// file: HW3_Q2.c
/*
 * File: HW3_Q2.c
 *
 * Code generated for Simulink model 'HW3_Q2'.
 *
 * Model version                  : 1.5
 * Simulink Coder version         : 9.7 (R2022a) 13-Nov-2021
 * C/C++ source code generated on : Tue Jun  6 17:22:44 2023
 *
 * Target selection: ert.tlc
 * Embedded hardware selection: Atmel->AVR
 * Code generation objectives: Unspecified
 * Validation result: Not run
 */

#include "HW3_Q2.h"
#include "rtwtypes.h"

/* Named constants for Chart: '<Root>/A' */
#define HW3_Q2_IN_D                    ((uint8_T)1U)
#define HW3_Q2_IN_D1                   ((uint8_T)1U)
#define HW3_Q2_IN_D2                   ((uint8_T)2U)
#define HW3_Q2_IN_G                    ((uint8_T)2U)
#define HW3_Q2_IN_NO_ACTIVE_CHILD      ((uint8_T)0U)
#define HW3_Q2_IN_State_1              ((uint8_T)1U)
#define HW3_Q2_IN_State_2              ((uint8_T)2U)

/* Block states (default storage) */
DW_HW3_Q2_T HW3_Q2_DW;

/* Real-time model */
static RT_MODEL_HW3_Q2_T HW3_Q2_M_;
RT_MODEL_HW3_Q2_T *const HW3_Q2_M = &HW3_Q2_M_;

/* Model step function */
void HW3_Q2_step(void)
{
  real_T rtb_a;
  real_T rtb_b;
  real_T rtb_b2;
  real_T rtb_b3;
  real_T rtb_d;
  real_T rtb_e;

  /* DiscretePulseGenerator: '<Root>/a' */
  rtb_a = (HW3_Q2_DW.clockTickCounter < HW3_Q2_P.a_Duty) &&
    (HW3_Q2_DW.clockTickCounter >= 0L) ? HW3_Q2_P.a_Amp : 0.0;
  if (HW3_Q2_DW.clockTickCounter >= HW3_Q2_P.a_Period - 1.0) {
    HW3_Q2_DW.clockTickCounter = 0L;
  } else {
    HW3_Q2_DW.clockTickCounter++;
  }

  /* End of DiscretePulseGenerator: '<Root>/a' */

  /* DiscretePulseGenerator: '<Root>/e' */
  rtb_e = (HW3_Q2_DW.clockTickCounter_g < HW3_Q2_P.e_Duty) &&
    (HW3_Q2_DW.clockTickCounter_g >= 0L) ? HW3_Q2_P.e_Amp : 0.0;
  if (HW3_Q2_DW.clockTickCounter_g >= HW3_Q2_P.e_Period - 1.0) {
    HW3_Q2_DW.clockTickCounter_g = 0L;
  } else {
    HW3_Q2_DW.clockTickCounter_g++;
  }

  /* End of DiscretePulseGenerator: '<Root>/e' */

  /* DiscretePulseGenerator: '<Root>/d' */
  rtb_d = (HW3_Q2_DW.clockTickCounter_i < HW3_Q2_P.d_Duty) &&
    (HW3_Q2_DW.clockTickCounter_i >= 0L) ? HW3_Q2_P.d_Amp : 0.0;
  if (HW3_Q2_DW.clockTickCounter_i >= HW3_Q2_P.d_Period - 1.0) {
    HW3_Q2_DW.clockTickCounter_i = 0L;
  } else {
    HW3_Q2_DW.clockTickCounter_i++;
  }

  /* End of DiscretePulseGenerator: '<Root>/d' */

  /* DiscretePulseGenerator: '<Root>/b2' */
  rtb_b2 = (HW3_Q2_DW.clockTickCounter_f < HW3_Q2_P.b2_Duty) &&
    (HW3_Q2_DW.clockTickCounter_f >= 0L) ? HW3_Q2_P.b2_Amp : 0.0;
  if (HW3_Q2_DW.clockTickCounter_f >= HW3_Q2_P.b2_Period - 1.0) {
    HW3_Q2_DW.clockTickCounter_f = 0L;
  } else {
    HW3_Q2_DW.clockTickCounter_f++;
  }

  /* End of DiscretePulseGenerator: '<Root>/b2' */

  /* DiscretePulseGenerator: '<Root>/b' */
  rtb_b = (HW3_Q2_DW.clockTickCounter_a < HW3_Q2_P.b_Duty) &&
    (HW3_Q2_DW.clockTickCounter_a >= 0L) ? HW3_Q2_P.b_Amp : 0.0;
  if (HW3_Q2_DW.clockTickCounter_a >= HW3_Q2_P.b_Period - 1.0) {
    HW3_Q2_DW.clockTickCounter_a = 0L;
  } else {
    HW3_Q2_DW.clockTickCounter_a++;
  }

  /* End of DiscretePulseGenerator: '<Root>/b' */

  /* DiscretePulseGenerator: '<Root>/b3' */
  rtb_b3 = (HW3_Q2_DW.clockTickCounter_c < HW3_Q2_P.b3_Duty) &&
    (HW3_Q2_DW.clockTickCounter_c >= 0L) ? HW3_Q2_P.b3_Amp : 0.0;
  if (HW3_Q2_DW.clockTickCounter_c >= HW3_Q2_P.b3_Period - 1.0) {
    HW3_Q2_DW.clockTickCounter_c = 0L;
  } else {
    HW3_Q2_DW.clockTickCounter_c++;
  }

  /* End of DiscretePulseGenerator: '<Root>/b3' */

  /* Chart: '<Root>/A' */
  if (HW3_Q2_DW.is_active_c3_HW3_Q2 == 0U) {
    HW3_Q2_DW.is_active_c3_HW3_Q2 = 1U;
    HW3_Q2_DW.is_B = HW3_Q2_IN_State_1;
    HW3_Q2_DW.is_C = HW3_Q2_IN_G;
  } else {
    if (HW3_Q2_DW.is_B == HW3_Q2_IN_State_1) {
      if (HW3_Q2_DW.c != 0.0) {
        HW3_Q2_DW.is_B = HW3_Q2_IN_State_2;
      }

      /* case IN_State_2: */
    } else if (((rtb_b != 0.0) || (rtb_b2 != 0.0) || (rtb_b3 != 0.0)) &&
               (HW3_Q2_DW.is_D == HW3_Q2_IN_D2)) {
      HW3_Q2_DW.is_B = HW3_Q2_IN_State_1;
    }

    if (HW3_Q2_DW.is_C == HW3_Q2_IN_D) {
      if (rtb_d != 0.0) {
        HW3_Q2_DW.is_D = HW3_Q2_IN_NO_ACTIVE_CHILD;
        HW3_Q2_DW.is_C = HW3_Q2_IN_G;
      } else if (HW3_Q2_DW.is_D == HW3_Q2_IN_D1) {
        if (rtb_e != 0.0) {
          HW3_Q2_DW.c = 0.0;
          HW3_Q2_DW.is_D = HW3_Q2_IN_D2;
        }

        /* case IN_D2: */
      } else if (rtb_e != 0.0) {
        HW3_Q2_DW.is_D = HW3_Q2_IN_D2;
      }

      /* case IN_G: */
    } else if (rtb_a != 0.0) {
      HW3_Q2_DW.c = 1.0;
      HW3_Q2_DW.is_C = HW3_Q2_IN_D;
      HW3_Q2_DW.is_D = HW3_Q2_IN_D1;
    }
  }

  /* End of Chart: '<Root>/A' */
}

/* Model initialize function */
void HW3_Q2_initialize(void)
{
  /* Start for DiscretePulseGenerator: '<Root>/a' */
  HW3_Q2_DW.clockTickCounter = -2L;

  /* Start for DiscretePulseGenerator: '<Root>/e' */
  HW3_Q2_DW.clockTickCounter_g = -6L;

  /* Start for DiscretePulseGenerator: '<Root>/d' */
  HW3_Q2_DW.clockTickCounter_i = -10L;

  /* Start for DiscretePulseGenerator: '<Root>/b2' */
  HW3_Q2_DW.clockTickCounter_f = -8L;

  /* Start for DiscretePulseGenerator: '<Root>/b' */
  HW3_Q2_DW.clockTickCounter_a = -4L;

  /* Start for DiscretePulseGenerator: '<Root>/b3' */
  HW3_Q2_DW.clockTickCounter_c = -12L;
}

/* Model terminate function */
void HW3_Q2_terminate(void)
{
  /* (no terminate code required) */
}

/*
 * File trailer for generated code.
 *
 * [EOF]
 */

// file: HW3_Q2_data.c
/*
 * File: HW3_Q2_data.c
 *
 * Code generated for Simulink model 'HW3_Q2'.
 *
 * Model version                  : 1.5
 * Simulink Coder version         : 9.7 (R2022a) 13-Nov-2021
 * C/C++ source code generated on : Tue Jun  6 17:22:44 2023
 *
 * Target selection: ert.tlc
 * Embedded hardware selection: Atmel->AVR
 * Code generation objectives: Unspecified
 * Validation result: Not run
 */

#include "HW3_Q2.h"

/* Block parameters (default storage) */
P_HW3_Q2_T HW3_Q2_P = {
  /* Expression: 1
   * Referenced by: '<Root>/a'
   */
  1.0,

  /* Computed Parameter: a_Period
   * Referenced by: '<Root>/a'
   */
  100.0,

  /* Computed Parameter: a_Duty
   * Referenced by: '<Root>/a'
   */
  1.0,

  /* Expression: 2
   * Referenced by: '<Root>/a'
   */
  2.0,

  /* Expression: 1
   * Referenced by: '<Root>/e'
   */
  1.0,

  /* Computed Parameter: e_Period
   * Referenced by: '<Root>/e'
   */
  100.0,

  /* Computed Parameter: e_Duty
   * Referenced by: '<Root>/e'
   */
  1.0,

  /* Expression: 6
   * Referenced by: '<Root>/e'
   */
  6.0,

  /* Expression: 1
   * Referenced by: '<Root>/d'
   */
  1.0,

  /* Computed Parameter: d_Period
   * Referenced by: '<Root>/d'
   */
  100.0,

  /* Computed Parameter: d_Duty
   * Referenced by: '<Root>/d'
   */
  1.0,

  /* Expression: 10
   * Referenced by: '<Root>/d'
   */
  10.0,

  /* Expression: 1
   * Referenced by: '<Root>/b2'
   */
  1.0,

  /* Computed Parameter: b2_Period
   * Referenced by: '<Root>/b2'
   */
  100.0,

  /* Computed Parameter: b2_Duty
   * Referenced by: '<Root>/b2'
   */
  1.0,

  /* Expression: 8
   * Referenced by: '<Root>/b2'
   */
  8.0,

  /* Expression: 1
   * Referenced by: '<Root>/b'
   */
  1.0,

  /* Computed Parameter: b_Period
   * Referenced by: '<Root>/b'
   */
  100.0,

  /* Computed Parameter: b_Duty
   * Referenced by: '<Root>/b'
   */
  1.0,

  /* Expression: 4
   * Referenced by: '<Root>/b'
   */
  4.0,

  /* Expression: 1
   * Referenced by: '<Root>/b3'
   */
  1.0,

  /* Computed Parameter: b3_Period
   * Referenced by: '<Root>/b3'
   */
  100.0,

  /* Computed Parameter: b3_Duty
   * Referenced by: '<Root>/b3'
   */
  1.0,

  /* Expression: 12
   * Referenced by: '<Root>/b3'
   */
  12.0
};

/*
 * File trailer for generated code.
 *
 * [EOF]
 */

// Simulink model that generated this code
simulink model "HW3_Q2"  (R2022a)
settings: Solver=FixedStepDiscrete  StartTime=0.0  StopTime=20  FixedStep=1  RelTol=1e-3  EnableMultiTasking=on

== system HW3_Q2 ==
  A : Stateflow chart  TreatAsAtomicUnit=on
  a : DiscretePulseGenerator  PulseType=Time based  Period=100  PhaseDelay=2
  b : DiscretePulseGenerator  PulseType=Time based  Period=100  PhaseDelay=4
  b2 : DiscretePulseGenerator  PulseType=Time based  Period=100  PhaseDelay=8
  b3 : DiscretePulseGenerator  PulseType=Time based  Period=100  PhaseDelay=12
  d : DiscretePulseGenerator  PulseType=Time based  Period=100  PhaseDelay=10
  e : DiscretePulseGenerator  PulseType=Time based  Period=100  PhaseDelay=6
  wires:
  a/1 -> A/1(a)
  b/1 -> A/5(b)
  e/1 -> A/2(e)
  b2/1 -> A/4(b2)
  d/1 -> A/3(d)
  b3/1 -> A/6(b3)

== stateflow chart HW3_Q2/A ==
  state B [parallel]
    settings: executionOrder=1
    state State_1
    state State_2
    (default) -> State_1
    State_1 -> State_2 : [c]
    State_2 -> State_1 : [(b || b2 || b3) && in(C.D.D2)]
  state C [parallel]
    settings: executionOrder=2
    state D
      state D1
      state D2
      (default) -> D1
      D1 -> D2 : [e]{c = 0;}
      D2 -> D2 : [e]
    state G
    G -> D : [a]{c = 1;}
    (default) -> G
    D -> G : [d]
  data: a input; e input; d input; b2 input; b input; c local =0; b3 input
